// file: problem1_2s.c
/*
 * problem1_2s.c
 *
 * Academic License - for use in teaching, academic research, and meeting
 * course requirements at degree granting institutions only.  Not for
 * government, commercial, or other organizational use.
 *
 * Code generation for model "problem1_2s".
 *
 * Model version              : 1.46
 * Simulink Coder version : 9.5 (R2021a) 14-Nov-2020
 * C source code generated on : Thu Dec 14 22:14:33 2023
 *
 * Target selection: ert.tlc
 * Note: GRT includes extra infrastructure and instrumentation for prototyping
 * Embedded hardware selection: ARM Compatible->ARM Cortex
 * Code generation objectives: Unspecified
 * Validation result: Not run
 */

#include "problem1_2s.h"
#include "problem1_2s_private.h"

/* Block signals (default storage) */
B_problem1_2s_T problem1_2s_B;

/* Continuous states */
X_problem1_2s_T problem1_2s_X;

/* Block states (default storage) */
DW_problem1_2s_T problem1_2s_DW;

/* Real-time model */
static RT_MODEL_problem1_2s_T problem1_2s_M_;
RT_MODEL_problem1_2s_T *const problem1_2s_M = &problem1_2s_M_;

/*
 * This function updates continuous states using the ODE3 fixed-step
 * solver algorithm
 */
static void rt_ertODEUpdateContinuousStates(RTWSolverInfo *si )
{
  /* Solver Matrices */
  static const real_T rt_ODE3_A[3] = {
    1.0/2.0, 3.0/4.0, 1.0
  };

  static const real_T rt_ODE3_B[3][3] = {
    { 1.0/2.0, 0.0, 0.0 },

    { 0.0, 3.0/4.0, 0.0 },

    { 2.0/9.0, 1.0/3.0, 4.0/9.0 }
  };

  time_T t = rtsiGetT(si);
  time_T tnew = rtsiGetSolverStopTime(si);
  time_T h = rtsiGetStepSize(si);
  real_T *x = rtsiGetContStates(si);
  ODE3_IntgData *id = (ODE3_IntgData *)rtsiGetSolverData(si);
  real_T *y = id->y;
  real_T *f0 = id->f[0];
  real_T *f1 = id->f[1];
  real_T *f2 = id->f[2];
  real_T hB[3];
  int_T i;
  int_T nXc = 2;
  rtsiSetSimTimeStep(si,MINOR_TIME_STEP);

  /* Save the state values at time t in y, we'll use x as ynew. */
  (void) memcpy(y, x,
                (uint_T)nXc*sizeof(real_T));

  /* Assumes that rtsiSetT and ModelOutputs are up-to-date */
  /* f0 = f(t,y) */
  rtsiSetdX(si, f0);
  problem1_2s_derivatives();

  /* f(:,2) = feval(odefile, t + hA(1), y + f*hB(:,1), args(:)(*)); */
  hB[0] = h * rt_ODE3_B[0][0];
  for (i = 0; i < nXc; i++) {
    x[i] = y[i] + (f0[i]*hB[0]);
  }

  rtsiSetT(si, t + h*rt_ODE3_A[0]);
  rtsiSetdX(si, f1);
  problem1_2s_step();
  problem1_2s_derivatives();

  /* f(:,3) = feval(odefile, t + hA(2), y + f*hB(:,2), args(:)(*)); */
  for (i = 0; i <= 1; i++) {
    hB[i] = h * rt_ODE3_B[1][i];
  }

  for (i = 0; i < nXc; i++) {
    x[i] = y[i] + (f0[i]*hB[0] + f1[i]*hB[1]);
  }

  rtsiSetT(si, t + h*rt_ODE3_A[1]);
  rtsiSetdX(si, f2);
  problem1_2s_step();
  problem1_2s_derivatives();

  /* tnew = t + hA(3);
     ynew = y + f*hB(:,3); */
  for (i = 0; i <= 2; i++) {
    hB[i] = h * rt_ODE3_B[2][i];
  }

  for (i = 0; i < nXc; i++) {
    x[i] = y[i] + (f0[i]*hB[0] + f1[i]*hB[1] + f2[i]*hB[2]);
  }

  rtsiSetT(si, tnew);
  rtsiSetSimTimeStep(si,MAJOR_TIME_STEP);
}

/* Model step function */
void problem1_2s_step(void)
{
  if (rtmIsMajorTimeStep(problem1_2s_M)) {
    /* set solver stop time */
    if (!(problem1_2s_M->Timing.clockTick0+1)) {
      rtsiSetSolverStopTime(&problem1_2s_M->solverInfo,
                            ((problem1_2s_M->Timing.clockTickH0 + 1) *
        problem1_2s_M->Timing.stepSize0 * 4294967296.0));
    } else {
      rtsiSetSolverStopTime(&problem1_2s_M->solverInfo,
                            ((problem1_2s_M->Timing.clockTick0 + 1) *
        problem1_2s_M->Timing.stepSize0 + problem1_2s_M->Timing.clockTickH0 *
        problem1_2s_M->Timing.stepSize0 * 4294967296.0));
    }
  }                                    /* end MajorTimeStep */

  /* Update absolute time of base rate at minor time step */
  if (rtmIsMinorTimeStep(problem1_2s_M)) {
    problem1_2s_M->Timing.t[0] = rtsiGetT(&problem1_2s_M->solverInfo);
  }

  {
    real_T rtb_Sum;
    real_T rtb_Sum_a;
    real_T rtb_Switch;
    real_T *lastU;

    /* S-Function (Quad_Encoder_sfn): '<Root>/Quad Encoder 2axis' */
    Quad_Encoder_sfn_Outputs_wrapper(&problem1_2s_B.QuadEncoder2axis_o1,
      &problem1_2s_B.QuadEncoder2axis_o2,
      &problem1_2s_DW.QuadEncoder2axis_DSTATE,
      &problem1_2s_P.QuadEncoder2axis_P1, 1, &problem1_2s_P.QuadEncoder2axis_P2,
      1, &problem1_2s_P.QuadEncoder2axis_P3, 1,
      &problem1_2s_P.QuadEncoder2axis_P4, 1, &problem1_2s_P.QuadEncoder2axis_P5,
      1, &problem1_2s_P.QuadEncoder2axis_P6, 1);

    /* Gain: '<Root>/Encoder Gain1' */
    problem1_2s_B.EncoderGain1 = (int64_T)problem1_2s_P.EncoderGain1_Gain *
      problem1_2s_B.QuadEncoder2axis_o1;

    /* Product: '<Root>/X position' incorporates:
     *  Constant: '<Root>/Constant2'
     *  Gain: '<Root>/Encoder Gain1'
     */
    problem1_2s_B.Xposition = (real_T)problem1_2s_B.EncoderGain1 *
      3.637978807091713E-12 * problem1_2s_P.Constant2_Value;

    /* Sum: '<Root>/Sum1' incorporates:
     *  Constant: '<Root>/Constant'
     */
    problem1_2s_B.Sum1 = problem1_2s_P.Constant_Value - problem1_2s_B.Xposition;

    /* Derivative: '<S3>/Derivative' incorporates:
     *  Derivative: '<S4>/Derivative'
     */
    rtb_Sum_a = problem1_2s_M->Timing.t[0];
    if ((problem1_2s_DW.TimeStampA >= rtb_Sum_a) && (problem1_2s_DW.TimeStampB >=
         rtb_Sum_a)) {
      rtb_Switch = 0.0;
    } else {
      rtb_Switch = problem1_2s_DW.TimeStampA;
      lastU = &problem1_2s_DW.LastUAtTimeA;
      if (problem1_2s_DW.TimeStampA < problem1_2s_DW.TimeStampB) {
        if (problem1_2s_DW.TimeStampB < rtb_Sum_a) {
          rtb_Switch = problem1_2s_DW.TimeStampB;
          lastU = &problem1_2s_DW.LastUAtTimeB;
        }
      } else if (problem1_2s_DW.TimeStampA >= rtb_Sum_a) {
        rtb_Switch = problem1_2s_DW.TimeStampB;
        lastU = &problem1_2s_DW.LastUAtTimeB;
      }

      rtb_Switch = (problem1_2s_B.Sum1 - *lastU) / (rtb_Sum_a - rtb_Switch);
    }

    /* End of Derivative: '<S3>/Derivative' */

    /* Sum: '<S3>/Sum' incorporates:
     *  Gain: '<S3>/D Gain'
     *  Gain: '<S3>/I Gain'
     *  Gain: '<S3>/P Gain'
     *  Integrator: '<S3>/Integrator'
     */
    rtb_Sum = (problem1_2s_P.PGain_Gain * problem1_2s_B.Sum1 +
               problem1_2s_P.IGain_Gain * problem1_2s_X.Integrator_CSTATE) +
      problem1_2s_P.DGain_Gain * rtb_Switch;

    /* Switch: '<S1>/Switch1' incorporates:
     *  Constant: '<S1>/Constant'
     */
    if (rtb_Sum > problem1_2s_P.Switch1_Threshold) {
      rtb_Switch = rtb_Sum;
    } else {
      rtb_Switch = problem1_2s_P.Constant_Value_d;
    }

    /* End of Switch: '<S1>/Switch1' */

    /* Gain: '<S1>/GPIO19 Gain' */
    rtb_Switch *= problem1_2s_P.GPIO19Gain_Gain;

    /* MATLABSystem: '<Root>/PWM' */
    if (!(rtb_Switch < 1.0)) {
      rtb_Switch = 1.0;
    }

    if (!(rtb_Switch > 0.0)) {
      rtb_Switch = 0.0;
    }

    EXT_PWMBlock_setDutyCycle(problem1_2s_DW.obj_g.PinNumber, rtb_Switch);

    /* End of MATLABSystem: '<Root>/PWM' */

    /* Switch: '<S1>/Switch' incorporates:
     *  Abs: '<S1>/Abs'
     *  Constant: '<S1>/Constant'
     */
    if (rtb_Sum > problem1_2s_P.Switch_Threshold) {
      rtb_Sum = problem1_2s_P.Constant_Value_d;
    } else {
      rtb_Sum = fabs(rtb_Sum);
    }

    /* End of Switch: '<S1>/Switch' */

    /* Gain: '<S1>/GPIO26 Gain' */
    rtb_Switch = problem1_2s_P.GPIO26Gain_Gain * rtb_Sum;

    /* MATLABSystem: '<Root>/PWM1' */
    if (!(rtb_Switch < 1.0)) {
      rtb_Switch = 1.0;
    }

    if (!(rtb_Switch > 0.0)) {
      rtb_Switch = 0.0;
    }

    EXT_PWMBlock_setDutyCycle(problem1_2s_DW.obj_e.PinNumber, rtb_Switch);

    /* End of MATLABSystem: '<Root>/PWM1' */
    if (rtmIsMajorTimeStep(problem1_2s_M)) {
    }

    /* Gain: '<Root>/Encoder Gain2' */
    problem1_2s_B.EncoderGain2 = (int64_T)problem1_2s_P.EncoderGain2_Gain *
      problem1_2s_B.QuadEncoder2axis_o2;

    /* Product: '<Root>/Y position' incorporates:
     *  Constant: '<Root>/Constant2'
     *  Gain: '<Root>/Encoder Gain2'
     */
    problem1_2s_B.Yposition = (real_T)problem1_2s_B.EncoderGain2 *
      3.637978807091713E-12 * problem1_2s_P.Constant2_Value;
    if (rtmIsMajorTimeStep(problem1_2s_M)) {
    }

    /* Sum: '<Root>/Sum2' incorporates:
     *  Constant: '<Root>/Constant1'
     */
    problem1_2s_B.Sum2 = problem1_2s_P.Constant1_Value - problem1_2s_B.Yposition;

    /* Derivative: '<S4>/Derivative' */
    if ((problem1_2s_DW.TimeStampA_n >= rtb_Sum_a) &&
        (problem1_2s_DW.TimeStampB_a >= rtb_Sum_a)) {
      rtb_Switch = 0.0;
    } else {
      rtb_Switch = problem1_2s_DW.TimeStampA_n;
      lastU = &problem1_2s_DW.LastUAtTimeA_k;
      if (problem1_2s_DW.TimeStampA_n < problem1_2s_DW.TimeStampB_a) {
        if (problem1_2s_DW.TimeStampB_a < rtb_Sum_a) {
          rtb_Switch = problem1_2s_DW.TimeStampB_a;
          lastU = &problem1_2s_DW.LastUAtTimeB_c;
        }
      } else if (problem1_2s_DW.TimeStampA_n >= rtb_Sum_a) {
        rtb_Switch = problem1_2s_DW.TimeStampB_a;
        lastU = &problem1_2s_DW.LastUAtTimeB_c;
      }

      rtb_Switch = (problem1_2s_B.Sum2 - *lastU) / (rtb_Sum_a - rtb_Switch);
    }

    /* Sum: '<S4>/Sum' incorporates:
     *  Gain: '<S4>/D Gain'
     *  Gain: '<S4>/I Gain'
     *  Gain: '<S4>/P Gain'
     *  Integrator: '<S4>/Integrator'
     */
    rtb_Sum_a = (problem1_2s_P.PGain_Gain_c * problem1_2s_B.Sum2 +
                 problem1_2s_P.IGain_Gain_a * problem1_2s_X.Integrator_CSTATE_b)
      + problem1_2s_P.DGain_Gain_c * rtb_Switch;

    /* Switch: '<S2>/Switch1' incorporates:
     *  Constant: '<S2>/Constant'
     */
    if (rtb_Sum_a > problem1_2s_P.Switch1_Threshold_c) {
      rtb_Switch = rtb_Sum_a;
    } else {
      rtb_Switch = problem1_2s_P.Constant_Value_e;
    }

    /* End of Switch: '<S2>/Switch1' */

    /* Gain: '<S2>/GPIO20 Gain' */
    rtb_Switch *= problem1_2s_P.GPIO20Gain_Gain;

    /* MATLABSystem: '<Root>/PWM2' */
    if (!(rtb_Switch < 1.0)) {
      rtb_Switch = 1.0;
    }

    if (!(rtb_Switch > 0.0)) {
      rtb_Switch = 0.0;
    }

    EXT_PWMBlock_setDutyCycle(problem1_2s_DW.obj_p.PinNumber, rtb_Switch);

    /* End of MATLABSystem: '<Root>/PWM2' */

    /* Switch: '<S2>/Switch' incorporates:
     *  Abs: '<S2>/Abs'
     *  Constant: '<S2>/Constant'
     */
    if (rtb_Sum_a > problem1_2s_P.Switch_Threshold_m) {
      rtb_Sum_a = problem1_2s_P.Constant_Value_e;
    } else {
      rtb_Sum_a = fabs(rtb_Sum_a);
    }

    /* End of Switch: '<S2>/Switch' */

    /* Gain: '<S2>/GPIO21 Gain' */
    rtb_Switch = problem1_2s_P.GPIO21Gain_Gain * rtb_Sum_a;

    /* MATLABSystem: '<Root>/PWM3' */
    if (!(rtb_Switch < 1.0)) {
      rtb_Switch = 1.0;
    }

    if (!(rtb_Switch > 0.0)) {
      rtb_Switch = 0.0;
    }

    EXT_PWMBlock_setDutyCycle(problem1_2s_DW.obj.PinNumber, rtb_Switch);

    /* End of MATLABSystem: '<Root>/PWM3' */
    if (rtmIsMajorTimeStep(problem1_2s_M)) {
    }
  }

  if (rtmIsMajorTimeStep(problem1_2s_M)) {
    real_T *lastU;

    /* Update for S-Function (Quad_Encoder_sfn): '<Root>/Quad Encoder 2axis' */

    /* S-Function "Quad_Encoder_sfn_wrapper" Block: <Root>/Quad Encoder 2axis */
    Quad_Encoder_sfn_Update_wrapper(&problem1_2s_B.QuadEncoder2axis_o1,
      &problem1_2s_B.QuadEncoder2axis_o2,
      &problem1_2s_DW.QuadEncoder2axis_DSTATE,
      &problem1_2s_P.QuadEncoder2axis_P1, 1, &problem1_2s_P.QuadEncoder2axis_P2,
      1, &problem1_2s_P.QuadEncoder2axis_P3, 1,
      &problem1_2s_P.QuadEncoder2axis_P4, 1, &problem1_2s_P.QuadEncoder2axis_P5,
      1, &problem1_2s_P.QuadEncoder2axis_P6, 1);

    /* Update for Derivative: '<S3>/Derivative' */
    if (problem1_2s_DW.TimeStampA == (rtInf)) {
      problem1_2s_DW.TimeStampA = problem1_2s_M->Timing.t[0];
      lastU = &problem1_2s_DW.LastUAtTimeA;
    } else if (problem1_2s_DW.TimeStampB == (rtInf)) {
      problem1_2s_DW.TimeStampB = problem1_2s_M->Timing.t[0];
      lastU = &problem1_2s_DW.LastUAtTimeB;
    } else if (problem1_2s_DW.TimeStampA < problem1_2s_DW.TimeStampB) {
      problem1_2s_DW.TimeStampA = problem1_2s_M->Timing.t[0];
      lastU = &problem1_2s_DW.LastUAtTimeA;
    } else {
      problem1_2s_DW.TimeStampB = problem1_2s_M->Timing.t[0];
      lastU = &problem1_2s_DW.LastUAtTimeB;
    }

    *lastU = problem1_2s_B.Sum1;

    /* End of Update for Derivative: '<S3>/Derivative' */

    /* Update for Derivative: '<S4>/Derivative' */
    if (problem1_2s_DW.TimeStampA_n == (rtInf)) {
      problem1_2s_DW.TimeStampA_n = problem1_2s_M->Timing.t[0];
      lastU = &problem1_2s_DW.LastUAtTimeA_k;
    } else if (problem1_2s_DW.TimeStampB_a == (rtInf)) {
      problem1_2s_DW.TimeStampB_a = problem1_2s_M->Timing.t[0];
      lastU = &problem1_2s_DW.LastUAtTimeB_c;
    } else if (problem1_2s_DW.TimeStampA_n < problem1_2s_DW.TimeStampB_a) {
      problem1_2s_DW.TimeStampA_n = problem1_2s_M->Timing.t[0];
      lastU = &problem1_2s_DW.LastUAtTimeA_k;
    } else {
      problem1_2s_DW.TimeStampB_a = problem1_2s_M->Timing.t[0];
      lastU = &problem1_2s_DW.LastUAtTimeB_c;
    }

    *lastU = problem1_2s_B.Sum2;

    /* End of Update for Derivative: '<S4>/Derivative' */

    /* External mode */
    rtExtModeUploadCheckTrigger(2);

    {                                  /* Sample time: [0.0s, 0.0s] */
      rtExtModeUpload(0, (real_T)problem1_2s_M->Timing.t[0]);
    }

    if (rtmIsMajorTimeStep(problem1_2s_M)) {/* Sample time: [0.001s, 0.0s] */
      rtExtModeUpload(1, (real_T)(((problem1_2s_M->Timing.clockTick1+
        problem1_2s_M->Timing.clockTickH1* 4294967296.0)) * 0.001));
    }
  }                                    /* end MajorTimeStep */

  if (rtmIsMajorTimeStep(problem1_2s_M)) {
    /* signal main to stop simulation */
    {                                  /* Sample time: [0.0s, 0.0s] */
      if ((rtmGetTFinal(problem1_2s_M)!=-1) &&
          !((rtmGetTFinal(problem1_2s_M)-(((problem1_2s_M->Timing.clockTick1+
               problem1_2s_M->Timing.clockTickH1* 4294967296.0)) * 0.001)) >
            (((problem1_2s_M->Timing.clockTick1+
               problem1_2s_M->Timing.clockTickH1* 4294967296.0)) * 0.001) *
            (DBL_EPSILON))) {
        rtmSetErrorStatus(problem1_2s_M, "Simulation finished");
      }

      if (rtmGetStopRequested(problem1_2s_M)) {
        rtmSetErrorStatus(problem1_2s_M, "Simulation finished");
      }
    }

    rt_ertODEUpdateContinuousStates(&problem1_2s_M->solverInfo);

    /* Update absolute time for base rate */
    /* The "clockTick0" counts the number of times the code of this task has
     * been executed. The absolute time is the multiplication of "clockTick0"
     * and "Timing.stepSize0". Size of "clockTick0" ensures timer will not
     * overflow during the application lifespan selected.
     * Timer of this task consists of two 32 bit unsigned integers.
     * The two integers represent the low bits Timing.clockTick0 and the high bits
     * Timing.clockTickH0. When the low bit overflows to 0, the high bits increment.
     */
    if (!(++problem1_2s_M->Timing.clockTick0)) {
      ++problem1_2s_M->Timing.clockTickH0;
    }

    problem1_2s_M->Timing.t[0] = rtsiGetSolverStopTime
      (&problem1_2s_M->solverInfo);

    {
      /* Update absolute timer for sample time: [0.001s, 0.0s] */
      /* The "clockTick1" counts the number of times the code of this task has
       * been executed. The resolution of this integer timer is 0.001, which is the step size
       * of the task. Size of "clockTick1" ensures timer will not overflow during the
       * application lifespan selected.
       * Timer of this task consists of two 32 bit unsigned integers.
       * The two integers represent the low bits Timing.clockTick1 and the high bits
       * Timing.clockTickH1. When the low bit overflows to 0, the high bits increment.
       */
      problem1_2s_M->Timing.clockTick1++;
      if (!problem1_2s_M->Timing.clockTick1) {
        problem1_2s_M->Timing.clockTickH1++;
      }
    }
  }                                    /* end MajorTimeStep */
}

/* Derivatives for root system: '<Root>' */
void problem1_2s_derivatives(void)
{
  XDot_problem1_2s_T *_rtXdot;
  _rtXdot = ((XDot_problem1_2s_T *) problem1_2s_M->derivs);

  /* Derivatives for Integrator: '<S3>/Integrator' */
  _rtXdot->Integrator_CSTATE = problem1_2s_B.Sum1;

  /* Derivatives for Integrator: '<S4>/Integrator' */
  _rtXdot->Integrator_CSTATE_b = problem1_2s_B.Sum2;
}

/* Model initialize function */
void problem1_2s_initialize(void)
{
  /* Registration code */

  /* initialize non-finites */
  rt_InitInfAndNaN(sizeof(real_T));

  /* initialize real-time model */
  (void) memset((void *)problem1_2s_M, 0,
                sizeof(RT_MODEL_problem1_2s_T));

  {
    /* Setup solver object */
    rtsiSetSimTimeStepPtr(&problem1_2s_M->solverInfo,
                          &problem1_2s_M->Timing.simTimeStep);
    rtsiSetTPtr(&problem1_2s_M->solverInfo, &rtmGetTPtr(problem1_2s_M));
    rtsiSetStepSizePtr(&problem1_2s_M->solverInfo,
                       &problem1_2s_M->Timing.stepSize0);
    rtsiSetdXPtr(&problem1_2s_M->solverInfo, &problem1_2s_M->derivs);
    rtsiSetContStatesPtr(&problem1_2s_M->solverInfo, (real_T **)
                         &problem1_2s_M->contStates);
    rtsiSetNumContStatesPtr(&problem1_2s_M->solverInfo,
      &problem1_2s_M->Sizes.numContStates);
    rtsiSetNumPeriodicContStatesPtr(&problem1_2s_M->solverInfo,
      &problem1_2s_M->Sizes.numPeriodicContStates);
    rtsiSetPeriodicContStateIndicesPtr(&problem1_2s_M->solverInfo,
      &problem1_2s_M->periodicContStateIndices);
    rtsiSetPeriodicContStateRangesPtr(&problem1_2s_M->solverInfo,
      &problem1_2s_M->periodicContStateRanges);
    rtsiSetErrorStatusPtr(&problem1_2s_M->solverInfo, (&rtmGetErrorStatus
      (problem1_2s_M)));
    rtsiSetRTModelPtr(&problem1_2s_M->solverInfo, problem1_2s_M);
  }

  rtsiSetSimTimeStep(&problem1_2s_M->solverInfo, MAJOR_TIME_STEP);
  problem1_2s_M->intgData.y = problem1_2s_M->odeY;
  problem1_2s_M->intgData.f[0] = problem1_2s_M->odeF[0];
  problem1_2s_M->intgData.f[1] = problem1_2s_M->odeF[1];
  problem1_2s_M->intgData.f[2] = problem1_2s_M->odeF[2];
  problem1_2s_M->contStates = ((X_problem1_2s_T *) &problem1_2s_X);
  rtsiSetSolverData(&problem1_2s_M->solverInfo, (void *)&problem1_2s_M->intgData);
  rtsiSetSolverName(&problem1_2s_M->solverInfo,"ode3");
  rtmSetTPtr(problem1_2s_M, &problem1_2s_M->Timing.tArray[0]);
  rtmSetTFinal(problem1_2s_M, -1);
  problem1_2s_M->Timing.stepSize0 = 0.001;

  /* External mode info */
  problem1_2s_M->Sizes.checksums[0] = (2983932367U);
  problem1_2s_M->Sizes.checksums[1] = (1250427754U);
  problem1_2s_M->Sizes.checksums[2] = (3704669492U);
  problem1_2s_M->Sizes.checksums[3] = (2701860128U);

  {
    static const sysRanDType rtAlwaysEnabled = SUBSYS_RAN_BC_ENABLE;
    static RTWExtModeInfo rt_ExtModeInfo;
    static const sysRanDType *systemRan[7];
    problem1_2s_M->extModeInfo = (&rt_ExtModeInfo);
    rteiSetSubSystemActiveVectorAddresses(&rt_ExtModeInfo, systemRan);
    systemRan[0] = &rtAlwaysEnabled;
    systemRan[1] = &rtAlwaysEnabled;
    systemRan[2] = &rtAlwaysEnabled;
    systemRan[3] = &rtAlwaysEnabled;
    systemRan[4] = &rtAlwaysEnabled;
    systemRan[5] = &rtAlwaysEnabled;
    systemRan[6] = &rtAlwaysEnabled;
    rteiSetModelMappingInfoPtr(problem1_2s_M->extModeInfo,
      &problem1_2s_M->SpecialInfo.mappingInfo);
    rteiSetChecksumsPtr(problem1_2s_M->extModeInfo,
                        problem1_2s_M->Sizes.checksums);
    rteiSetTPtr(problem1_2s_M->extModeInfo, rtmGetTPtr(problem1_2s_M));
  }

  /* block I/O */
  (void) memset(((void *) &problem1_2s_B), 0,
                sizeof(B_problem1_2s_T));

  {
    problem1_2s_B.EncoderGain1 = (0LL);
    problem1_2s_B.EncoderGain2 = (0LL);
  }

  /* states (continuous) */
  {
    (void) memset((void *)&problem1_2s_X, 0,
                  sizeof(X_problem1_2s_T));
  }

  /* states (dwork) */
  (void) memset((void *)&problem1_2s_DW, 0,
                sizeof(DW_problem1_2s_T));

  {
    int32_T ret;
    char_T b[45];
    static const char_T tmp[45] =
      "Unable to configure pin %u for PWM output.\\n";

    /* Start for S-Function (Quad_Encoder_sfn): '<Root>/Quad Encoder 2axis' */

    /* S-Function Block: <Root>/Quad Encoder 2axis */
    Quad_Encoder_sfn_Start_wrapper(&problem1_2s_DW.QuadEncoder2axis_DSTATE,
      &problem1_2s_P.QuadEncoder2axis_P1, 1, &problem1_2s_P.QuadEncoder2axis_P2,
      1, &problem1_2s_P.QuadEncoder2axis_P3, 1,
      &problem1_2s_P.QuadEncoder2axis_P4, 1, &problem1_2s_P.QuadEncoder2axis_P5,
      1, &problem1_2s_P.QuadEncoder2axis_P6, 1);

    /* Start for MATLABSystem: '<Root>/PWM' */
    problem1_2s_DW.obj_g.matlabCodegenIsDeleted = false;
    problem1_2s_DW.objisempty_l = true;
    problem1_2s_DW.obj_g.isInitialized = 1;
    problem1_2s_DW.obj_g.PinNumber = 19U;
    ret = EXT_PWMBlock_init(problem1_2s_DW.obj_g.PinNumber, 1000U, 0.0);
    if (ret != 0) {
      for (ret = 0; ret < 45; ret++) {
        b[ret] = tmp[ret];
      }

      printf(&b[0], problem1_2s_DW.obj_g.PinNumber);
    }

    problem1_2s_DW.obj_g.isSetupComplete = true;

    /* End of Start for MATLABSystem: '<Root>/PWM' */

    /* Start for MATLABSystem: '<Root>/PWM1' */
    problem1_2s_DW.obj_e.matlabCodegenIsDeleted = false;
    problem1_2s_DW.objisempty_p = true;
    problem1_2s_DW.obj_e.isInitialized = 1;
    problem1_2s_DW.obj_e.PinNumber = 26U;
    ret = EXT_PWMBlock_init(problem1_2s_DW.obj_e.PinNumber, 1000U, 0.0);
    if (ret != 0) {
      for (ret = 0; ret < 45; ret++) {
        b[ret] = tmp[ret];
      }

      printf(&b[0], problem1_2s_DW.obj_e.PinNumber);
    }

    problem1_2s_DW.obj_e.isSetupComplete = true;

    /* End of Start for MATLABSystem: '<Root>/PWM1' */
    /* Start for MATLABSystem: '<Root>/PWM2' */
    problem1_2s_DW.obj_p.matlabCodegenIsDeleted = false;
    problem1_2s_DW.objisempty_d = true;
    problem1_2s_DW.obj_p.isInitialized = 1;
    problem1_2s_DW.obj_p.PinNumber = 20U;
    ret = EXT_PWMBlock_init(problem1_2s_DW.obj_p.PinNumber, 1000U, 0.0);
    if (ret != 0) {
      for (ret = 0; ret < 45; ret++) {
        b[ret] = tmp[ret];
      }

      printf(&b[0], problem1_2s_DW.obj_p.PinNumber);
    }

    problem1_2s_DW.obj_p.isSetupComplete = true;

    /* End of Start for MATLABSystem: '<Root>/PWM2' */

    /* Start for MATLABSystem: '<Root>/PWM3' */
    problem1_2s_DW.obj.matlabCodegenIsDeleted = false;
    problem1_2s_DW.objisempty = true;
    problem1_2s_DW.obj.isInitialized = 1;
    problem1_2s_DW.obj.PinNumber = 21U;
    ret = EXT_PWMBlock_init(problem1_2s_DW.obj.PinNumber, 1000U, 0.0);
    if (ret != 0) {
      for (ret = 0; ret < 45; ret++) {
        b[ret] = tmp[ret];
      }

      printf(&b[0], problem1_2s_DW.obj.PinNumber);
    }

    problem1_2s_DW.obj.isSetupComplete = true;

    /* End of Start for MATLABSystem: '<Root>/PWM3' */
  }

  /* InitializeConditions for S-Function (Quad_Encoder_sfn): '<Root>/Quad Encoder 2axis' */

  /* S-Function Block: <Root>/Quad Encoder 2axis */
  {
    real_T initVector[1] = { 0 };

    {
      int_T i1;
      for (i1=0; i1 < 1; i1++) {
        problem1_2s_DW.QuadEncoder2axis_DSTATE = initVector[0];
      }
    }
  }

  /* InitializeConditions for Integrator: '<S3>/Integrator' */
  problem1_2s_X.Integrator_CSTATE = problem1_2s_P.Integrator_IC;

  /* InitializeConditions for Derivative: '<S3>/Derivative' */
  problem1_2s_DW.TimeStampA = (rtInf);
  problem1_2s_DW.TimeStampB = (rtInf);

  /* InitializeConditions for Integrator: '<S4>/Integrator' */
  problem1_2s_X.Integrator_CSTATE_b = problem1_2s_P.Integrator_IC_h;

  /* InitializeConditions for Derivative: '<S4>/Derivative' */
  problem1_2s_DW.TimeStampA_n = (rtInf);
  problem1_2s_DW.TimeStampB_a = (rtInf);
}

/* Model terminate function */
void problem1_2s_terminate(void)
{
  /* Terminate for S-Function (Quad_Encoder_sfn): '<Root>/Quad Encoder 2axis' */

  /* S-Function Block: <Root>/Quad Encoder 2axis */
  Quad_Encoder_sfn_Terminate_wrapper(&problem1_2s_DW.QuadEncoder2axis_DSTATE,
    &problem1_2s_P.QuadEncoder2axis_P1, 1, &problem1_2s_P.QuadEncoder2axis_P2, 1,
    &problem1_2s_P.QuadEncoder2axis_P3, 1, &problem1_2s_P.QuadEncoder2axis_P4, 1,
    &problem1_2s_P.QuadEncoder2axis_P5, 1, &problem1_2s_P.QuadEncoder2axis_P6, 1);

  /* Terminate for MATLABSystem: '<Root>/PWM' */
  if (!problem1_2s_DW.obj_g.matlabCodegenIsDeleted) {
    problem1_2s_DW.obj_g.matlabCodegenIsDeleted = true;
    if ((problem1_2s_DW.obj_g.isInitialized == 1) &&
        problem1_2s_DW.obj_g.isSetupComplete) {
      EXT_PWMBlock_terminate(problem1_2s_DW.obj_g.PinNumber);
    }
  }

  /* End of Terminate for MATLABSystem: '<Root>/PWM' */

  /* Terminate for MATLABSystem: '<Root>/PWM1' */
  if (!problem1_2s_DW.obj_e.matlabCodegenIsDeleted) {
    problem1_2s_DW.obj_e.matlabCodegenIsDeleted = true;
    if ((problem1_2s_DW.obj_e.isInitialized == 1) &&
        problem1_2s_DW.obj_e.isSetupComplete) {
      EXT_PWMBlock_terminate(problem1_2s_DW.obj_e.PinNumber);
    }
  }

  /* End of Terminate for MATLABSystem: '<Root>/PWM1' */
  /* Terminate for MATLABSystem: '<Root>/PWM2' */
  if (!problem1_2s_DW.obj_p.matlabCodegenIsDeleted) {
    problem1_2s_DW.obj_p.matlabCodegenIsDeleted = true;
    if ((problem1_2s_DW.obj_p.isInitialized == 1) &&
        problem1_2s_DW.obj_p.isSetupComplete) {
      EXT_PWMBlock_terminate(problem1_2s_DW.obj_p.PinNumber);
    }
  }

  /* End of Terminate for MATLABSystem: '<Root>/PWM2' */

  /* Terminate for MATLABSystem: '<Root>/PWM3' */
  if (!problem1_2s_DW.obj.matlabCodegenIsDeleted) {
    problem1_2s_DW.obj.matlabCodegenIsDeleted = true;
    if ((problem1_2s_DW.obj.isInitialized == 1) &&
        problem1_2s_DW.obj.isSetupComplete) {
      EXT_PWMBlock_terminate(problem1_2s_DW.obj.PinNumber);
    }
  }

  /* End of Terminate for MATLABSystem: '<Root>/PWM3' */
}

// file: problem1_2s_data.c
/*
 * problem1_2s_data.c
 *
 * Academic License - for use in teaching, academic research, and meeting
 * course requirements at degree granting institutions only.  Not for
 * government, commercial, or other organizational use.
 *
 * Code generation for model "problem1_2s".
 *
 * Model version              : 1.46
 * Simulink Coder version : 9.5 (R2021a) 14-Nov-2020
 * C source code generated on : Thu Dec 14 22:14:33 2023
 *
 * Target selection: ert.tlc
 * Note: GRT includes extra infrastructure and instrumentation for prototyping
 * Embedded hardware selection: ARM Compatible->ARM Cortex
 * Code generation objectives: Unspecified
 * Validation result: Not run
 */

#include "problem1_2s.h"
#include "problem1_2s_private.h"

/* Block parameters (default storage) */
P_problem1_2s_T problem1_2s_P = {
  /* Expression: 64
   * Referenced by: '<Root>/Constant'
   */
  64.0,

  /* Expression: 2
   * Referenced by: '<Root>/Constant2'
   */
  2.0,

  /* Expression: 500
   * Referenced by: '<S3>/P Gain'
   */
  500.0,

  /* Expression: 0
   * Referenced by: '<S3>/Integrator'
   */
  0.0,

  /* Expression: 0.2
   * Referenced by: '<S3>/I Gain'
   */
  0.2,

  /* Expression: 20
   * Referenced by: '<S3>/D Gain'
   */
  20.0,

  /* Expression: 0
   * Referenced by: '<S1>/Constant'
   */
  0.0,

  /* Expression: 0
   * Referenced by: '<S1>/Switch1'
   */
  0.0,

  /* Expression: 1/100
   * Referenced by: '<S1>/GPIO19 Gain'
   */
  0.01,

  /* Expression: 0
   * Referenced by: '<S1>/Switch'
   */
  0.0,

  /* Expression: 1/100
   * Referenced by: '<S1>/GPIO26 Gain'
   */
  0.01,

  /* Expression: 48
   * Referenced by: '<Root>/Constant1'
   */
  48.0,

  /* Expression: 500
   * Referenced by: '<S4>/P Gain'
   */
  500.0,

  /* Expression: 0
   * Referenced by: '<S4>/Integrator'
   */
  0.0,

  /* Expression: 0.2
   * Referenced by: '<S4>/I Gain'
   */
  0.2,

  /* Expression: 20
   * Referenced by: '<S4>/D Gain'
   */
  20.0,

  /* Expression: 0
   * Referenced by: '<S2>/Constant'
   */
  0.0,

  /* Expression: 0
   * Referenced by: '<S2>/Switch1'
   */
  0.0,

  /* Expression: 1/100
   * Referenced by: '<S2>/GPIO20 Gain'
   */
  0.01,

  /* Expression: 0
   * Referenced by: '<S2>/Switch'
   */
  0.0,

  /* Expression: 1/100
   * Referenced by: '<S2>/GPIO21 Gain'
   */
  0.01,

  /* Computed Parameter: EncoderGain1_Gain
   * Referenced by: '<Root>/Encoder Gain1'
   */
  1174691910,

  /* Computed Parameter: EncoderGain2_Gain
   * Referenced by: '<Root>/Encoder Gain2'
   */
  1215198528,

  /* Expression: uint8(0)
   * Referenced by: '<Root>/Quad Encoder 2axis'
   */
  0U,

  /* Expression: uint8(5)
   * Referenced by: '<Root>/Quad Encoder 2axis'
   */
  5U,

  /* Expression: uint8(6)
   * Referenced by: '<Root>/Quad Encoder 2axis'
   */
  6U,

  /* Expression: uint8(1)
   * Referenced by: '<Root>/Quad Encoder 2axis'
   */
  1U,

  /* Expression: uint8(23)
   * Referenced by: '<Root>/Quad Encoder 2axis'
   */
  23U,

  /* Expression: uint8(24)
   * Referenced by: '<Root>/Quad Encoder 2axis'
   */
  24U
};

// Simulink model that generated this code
simulink model "problem1_2s"  (R2021a)
settings: Solver=FixedStepAuto  StartTime=0.0  StopTime=10  FixedStep=0.001  RelTol=1e-3  EnableMultiTasking=on
StopFcn:
  | mypi=raspi();
  | writeDigitalPin(mypi,19,0);
  | writeDigitalPin(mypi,26,0);
  | writeDigitalPin(mypi,20,0);
  | writeDigitalPin(mypi,21,0);
  | clear mypi;
libraries: raspberrypiBasiclib x4

== system problem1_2s ==
  note: Reference Position
  Constant : Constant  Value=64
  Constant1 : Constant  Value=48
  Constant2 : Constant  Value=2
  Encoder Gain1 : Gain  Gain=1/234
  Encoder Gain2 : Gain  Gain=1/226.2
  Motor Subsystem : Subsystem
  Motor Subsystem1 : Subsystem
  PID Subsystem : Subsystem
  PID Subsystem1 : Subsystem
  PWM : raspberrypiBasiclib/PWM  board=Pi 4 Model B  Pin_=19  Frequency=1000  blockPlatform=Raspberry Pi
  PWM1 : raspberrypiBasiclib/PWM  board=Pi 4 Model B  Pin_=26  Frequency=1000  blockPlatform=Raspberry Pi
  PWM2 : raspberrypiBasiclib/PWM  board=Pi 4 Model B  Pin_=20  Frequency=1000  blockPlatform=Raspberry Pi
  PWM3 : raspberrypiBasiclib/PWM  board=Pi 4 Model B  Pin_=21  Frequency=1000  blockPlatform=Raspberry Pi
  Quad Encoder 2axis : S-Function  InitFcn=try, set_param(gcb,'FunctionName','Quad_Encoder_sfn'), end  FunctionName=Quad_Encoder_sfn  Parameters=uint8(0),uint8(5),uint8(6),uint8(1),uint8(23),uint8(24)  SFunctionModules=Quad_Encoder_sfn_wrapper  SFunctionDeploymentMode=off  EnableBusSupport=off  mask(S-Function Builder){}
      mask init:
      | val = [[.9  0.75 0.75 1 1 .9 .9 1]',[1 1 0.75 0.75 .9 .9 1 .9]'];try , sys = get_param(gcb,'SfunBuilderFcnName');if isempty(sys), sys = get_param(gcb,'FunctionName'); end,catch, sys = get_param(gcb,'FunctionName'); end
  Sum1 : Sum  Inputs=|+-
  Sum2 : Sum  Inputs=-+|
  To Workspace1 : ToWorkspace  VariableName=xpos  SampleTime=0.001
  To Workspace2 : ToWorkspace  VariableName=ypos  SampleTime=0.001
  X position : Product  Inputs=**
  Y position : Product  Inputs=**
  wires:
  Quad Encoder 2axis/1 -> Encoder Gain1/1
  Quad Encoder 2axis/2 -> Encoder Gain2/1
  Sum1/1 -> PID Subsystem/1(In1)
  PID Subsystem/1(Out1) -> Motor Subsystem/1(In1)
  Motor Subsystem/1(Out1) -> PWM/1
  Motor Subsystem/2(Out2) -> PWM1/1
  Motor Subsystem1/2(Out2) -> PWM3/1
  Motor Subsystem1/1(Out1) -> PWM2/1
  PID Subsystem1/1(Out1) -> Motor Subsystem1/1(In1)
  Sum2/1 -> PID Subsystem1/1(In1)
  Constant/1 -> Sum1/1
  Constant1/1 -> Sum2/2
  Encoder Gain1/1 -> X position/1
  X position/1 -> To Workspace1/1, Sum1/2
  Encoder Gain2/1 -> Y position/2
  Y position/1 -> To Workspace2/1, Sum2/1
  Constant2/1 -> Y position/1, X position/2

== system problem1_2s/Motor Subsystem ==
  In1 : Inport
  Abs : Abs
  Constant : Constant  Value=0
  GPIO19 Gain : Gain  Gain=1/100
  GPIO26 Gain : Gain  Gain=1/100
  Switch : Switch  Criteria=u2 > Threshold
  Switch1 : Switch  Criteria=u2 > Threshold
  Out1 : Outport
  Out2 : Outport  Port=2
  wires:
  Switch/1 -> GPIO26 Gain/1
  Abs/1 -> Switch/3
  Switch1/1 -> GPIO19 Gain/1
  In1/1 -> Abs/1, Switch/2, Switch1/1, Switch1/2
  Constant/1 -> Switch/1, Switch1/3
  GPIO26 Gain/1 -> Out2/1
  GPIO19 Gain/1 -> Out1/1

== system problem1_2s/Motor Subsystem1 ==
  In1 : Inport
  Abs : Abs
  Constant : Constant  Value=0
  GPIO20 Gain : Gain  Gain=1/100
  GPIO21 Gain : Gain  Gain=1/100
  Switch : Switch  Criteria=u2 > Threshold
  Switch1 : Switch  Criteria=u2 > Threshold
  Out1 : Outport
  Out2 : Outport  Port=2
  wires:
  Switch/1 -> GPIO21 Gain/1
  Abs/1 -> Switch/3
  Switch1/1 -> GPIO20 Gain/1
  In1/1 -> Abs/1, Switch/2, Switch1/1, Switch1/2
  Constant/1 -> Switch/1, Switch1/3
  GPIO21 Gain/1 -> Out2/1
  GPIO20 Gain/1 -> Out1/1

== system problem1_2s/PID Subsystem ==
  In1 : Inport
  D Gain : Gain  Gain=20
  Derivative : Derivative
  I Gain : Gain  Gain=0.2
  Integrator : Integrator
  P Gain : Gain  Gain=500
  Sum : Sum  Inputs=+++
  Out1 : Outport
  wires:
  Derivative/1 -> D Gain/1
  I Gain/1 -> Sum/2
  Integrator/1 -> I Gain/1
  P Gain/1 -> Sum/1
  D Gain/1 -> Sum/3
  Sum/1 -> Out1/1
  In1/1 -> P Gain/1, Derivative/1, Integrator/1

== system problem1_2s/PID Subsystem1 ==
  In1 : Inport
  D Gain : Gain  Gain=20
  Derivative : Derivative
  I Gain : Gain  Gain=0.2
  Integrator : Integrator
  P Gain : Gain  Gain=500
  Sum : Sum  Inputs=+++
  Out1 : Outport
  wires:
  Derivative/1 -> D Gain/1
  I Gain/1 -> Sum/2
  Integrator/1 -> I Gain/1
  P Gain/1 -> Sum/1
  D Gain/1 -> Sum/3
  Sum/1 -> Out1/1
  In1/1 -> P Gain/1, Derivative/1, Integrator/1
